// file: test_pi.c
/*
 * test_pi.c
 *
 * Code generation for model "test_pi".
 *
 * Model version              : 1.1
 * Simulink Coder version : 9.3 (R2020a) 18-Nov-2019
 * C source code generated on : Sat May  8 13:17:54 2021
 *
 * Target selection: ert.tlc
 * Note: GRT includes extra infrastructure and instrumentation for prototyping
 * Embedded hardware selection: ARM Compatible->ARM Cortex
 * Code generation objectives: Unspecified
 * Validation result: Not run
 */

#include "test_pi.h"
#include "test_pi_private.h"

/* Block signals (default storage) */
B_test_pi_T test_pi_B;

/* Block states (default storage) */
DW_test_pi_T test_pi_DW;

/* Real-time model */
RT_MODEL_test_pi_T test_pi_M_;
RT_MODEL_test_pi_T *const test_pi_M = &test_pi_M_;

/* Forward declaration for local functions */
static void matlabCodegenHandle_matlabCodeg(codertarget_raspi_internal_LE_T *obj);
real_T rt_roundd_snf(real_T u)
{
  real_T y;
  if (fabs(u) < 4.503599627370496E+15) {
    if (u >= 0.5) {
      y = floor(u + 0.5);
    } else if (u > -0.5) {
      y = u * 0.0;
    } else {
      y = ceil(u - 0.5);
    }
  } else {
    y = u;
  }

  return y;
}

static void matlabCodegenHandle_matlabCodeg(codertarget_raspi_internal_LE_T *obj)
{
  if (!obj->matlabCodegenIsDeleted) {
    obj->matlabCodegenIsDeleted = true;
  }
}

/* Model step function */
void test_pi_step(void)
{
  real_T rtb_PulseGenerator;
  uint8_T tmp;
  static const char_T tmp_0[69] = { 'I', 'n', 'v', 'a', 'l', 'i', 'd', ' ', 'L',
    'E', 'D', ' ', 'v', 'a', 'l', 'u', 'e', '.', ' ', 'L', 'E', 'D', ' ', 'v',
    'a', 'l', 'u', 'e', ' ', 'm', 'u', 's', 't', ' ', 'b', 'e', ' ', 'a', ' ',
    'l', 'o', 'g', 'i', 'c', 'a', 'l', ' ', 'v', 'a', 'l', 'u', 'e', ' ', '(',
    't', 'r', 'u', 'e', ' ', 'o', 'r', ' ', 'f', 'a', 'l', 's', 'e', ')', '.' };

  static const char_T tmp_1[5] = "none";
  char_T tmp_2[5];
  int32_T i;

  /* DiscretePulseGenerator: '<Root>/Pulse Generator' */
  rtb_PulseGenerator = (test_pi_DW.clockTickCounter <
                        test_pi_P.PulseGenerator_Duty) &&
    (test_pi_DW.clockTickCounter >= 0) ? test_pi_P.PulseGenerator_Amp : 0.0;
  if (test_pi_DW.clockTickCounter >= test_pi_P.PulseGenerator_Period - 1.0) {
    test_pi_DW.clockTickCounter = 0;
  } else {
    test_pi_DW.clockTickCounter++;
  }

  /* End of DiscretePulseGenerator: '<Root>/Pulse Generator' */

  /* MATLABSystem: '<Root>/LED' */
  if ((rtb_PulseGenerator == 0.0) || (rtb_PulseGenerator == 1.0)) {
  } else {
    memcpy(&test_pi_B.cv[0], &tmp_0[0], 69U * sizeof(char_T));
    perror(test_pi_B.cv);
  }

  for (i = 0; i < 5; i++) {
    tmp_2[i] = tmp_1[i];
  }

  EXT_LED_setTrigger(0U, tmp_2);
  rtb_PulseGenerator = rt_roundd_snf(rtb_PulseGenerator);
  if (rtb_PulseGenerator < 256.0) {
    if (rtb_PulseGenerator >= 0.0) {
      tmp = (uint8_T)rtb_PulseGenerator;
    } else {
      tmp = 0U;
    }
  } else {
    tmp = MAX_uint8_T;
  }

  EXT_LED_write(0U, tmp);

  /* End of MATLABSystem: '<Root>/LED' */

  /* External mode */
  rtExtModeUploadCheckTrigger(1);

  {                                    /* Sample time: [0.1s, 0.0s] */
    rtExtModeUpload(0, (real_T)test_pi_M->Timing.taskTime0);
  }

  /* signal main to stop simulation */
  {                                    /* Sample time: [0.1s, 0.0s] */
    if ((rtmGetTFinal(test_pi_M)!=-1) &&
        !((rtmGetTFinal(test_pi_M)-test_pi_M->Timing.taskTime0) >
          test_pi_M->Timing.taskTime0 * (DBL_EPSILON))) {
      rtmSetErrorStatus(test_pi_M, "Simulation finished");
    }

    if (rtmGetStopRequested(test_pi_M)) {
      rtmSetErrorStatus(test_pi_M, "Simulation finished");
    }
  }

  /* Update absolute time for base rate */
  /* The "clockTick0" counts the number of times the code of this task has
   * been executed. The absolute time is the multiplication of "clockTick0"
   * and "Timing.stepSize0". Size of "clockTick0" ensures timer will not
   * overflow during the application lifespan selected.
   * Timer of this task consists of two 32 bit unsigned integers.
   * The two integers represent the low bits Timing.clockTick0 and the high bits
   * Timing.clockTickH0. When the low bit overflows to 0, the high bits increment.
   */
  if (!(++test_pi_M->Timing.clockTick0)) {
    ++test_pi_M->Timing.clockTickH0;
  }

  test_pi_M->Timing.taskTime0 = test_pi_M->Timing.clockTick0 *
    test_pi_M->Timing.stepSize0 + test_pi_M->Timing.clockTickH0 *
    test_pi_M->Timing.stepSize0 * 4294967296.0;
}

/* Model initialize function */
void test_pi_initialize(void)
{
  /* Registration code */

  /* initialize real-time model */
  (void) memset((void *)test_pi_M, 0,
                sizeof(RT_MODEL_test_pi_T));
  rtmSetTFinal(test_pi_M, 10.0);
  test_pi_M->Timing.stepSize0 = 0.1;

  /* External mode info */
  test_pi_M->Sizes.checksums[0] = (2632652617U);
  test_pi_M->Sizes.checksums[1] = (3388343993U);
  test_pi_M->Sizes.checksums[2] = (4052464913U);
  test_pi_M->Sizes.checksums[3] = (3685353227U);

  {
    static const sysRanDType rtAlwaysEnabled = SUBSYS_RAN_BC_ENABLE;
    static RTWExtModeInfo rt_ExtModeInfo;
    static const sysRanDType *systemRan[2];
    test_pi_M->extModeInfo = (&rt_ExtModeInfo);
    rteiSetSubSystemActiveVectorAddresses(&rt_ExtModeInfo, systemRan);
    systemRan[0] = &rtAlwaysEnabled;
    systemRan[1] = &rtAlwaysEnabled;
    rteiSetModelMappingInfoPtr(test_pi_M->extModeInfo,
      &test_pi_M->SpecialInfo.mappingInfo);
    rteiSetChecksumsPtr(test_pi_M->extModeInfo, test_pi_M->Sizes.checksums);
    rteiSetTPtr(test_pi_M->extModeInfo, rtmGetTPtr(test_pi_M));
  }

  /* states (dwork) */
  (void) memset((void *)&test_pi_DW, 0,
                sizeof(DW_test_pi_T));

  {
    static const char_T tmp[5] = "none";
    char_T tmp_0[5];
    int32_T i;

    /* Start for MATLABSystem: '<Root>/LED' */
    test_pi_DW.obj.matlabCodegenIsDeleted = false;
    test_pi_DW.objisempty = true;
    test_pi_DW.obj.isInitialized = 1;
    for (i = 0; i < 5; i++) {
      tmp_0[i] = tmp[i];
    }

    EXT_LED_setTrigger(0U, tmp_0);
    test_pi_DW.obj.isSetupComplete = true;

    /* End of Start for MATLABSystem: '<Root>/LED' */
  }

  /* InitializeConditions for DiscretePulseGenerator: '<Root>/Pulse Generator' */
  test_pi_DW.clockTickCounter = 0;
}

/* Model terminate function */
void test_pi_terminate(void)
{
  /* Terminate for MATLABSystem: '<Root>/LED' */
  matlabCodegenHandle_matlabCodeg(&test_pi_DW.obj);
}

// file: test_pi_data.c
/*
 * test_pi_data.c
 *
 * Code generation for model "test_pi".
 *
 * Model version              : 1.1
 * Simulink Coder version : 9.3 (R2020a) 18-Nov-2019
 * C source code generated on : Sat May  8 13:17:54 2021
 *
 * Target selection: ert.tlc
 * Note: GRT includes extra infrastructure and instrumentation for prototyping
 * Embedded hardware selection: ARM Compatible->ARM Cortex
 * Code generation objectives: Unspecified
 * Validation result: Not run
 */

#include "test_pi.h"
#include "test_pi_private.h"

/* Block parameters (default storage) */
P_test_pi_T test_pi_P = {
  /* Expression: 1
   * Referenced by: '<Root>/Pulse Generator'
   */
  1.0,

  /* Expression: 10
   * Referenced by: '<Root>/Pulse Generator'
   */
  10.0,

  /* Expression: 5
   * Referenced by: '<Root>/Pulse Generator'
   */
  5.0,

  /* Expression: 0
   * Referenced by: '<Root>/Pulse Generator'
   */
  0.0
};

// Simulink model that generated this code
simulink model "test_pi"  (R2020a)
settings: Solver=ode5  StartTime=0.0  StopTime=10  FixedStep=0.1  RelTol=1e-3  EnableMultiTasking=on
undefined symbols (not defined in the file or in its folder): Green, led0
libraries: raspberrypiBasiclib x1

== system test_pi ==
  LED : raspberrypiBasiclib/LED  BoardProperty=Model B Rev2  LED_=led0 (Green)
  Pulse Generator : DiscretePulseGenerator  Period=10  PulseWidth=5  SampleTime=-1
  wires:
  Pulse Generator/1 -> LED/1
